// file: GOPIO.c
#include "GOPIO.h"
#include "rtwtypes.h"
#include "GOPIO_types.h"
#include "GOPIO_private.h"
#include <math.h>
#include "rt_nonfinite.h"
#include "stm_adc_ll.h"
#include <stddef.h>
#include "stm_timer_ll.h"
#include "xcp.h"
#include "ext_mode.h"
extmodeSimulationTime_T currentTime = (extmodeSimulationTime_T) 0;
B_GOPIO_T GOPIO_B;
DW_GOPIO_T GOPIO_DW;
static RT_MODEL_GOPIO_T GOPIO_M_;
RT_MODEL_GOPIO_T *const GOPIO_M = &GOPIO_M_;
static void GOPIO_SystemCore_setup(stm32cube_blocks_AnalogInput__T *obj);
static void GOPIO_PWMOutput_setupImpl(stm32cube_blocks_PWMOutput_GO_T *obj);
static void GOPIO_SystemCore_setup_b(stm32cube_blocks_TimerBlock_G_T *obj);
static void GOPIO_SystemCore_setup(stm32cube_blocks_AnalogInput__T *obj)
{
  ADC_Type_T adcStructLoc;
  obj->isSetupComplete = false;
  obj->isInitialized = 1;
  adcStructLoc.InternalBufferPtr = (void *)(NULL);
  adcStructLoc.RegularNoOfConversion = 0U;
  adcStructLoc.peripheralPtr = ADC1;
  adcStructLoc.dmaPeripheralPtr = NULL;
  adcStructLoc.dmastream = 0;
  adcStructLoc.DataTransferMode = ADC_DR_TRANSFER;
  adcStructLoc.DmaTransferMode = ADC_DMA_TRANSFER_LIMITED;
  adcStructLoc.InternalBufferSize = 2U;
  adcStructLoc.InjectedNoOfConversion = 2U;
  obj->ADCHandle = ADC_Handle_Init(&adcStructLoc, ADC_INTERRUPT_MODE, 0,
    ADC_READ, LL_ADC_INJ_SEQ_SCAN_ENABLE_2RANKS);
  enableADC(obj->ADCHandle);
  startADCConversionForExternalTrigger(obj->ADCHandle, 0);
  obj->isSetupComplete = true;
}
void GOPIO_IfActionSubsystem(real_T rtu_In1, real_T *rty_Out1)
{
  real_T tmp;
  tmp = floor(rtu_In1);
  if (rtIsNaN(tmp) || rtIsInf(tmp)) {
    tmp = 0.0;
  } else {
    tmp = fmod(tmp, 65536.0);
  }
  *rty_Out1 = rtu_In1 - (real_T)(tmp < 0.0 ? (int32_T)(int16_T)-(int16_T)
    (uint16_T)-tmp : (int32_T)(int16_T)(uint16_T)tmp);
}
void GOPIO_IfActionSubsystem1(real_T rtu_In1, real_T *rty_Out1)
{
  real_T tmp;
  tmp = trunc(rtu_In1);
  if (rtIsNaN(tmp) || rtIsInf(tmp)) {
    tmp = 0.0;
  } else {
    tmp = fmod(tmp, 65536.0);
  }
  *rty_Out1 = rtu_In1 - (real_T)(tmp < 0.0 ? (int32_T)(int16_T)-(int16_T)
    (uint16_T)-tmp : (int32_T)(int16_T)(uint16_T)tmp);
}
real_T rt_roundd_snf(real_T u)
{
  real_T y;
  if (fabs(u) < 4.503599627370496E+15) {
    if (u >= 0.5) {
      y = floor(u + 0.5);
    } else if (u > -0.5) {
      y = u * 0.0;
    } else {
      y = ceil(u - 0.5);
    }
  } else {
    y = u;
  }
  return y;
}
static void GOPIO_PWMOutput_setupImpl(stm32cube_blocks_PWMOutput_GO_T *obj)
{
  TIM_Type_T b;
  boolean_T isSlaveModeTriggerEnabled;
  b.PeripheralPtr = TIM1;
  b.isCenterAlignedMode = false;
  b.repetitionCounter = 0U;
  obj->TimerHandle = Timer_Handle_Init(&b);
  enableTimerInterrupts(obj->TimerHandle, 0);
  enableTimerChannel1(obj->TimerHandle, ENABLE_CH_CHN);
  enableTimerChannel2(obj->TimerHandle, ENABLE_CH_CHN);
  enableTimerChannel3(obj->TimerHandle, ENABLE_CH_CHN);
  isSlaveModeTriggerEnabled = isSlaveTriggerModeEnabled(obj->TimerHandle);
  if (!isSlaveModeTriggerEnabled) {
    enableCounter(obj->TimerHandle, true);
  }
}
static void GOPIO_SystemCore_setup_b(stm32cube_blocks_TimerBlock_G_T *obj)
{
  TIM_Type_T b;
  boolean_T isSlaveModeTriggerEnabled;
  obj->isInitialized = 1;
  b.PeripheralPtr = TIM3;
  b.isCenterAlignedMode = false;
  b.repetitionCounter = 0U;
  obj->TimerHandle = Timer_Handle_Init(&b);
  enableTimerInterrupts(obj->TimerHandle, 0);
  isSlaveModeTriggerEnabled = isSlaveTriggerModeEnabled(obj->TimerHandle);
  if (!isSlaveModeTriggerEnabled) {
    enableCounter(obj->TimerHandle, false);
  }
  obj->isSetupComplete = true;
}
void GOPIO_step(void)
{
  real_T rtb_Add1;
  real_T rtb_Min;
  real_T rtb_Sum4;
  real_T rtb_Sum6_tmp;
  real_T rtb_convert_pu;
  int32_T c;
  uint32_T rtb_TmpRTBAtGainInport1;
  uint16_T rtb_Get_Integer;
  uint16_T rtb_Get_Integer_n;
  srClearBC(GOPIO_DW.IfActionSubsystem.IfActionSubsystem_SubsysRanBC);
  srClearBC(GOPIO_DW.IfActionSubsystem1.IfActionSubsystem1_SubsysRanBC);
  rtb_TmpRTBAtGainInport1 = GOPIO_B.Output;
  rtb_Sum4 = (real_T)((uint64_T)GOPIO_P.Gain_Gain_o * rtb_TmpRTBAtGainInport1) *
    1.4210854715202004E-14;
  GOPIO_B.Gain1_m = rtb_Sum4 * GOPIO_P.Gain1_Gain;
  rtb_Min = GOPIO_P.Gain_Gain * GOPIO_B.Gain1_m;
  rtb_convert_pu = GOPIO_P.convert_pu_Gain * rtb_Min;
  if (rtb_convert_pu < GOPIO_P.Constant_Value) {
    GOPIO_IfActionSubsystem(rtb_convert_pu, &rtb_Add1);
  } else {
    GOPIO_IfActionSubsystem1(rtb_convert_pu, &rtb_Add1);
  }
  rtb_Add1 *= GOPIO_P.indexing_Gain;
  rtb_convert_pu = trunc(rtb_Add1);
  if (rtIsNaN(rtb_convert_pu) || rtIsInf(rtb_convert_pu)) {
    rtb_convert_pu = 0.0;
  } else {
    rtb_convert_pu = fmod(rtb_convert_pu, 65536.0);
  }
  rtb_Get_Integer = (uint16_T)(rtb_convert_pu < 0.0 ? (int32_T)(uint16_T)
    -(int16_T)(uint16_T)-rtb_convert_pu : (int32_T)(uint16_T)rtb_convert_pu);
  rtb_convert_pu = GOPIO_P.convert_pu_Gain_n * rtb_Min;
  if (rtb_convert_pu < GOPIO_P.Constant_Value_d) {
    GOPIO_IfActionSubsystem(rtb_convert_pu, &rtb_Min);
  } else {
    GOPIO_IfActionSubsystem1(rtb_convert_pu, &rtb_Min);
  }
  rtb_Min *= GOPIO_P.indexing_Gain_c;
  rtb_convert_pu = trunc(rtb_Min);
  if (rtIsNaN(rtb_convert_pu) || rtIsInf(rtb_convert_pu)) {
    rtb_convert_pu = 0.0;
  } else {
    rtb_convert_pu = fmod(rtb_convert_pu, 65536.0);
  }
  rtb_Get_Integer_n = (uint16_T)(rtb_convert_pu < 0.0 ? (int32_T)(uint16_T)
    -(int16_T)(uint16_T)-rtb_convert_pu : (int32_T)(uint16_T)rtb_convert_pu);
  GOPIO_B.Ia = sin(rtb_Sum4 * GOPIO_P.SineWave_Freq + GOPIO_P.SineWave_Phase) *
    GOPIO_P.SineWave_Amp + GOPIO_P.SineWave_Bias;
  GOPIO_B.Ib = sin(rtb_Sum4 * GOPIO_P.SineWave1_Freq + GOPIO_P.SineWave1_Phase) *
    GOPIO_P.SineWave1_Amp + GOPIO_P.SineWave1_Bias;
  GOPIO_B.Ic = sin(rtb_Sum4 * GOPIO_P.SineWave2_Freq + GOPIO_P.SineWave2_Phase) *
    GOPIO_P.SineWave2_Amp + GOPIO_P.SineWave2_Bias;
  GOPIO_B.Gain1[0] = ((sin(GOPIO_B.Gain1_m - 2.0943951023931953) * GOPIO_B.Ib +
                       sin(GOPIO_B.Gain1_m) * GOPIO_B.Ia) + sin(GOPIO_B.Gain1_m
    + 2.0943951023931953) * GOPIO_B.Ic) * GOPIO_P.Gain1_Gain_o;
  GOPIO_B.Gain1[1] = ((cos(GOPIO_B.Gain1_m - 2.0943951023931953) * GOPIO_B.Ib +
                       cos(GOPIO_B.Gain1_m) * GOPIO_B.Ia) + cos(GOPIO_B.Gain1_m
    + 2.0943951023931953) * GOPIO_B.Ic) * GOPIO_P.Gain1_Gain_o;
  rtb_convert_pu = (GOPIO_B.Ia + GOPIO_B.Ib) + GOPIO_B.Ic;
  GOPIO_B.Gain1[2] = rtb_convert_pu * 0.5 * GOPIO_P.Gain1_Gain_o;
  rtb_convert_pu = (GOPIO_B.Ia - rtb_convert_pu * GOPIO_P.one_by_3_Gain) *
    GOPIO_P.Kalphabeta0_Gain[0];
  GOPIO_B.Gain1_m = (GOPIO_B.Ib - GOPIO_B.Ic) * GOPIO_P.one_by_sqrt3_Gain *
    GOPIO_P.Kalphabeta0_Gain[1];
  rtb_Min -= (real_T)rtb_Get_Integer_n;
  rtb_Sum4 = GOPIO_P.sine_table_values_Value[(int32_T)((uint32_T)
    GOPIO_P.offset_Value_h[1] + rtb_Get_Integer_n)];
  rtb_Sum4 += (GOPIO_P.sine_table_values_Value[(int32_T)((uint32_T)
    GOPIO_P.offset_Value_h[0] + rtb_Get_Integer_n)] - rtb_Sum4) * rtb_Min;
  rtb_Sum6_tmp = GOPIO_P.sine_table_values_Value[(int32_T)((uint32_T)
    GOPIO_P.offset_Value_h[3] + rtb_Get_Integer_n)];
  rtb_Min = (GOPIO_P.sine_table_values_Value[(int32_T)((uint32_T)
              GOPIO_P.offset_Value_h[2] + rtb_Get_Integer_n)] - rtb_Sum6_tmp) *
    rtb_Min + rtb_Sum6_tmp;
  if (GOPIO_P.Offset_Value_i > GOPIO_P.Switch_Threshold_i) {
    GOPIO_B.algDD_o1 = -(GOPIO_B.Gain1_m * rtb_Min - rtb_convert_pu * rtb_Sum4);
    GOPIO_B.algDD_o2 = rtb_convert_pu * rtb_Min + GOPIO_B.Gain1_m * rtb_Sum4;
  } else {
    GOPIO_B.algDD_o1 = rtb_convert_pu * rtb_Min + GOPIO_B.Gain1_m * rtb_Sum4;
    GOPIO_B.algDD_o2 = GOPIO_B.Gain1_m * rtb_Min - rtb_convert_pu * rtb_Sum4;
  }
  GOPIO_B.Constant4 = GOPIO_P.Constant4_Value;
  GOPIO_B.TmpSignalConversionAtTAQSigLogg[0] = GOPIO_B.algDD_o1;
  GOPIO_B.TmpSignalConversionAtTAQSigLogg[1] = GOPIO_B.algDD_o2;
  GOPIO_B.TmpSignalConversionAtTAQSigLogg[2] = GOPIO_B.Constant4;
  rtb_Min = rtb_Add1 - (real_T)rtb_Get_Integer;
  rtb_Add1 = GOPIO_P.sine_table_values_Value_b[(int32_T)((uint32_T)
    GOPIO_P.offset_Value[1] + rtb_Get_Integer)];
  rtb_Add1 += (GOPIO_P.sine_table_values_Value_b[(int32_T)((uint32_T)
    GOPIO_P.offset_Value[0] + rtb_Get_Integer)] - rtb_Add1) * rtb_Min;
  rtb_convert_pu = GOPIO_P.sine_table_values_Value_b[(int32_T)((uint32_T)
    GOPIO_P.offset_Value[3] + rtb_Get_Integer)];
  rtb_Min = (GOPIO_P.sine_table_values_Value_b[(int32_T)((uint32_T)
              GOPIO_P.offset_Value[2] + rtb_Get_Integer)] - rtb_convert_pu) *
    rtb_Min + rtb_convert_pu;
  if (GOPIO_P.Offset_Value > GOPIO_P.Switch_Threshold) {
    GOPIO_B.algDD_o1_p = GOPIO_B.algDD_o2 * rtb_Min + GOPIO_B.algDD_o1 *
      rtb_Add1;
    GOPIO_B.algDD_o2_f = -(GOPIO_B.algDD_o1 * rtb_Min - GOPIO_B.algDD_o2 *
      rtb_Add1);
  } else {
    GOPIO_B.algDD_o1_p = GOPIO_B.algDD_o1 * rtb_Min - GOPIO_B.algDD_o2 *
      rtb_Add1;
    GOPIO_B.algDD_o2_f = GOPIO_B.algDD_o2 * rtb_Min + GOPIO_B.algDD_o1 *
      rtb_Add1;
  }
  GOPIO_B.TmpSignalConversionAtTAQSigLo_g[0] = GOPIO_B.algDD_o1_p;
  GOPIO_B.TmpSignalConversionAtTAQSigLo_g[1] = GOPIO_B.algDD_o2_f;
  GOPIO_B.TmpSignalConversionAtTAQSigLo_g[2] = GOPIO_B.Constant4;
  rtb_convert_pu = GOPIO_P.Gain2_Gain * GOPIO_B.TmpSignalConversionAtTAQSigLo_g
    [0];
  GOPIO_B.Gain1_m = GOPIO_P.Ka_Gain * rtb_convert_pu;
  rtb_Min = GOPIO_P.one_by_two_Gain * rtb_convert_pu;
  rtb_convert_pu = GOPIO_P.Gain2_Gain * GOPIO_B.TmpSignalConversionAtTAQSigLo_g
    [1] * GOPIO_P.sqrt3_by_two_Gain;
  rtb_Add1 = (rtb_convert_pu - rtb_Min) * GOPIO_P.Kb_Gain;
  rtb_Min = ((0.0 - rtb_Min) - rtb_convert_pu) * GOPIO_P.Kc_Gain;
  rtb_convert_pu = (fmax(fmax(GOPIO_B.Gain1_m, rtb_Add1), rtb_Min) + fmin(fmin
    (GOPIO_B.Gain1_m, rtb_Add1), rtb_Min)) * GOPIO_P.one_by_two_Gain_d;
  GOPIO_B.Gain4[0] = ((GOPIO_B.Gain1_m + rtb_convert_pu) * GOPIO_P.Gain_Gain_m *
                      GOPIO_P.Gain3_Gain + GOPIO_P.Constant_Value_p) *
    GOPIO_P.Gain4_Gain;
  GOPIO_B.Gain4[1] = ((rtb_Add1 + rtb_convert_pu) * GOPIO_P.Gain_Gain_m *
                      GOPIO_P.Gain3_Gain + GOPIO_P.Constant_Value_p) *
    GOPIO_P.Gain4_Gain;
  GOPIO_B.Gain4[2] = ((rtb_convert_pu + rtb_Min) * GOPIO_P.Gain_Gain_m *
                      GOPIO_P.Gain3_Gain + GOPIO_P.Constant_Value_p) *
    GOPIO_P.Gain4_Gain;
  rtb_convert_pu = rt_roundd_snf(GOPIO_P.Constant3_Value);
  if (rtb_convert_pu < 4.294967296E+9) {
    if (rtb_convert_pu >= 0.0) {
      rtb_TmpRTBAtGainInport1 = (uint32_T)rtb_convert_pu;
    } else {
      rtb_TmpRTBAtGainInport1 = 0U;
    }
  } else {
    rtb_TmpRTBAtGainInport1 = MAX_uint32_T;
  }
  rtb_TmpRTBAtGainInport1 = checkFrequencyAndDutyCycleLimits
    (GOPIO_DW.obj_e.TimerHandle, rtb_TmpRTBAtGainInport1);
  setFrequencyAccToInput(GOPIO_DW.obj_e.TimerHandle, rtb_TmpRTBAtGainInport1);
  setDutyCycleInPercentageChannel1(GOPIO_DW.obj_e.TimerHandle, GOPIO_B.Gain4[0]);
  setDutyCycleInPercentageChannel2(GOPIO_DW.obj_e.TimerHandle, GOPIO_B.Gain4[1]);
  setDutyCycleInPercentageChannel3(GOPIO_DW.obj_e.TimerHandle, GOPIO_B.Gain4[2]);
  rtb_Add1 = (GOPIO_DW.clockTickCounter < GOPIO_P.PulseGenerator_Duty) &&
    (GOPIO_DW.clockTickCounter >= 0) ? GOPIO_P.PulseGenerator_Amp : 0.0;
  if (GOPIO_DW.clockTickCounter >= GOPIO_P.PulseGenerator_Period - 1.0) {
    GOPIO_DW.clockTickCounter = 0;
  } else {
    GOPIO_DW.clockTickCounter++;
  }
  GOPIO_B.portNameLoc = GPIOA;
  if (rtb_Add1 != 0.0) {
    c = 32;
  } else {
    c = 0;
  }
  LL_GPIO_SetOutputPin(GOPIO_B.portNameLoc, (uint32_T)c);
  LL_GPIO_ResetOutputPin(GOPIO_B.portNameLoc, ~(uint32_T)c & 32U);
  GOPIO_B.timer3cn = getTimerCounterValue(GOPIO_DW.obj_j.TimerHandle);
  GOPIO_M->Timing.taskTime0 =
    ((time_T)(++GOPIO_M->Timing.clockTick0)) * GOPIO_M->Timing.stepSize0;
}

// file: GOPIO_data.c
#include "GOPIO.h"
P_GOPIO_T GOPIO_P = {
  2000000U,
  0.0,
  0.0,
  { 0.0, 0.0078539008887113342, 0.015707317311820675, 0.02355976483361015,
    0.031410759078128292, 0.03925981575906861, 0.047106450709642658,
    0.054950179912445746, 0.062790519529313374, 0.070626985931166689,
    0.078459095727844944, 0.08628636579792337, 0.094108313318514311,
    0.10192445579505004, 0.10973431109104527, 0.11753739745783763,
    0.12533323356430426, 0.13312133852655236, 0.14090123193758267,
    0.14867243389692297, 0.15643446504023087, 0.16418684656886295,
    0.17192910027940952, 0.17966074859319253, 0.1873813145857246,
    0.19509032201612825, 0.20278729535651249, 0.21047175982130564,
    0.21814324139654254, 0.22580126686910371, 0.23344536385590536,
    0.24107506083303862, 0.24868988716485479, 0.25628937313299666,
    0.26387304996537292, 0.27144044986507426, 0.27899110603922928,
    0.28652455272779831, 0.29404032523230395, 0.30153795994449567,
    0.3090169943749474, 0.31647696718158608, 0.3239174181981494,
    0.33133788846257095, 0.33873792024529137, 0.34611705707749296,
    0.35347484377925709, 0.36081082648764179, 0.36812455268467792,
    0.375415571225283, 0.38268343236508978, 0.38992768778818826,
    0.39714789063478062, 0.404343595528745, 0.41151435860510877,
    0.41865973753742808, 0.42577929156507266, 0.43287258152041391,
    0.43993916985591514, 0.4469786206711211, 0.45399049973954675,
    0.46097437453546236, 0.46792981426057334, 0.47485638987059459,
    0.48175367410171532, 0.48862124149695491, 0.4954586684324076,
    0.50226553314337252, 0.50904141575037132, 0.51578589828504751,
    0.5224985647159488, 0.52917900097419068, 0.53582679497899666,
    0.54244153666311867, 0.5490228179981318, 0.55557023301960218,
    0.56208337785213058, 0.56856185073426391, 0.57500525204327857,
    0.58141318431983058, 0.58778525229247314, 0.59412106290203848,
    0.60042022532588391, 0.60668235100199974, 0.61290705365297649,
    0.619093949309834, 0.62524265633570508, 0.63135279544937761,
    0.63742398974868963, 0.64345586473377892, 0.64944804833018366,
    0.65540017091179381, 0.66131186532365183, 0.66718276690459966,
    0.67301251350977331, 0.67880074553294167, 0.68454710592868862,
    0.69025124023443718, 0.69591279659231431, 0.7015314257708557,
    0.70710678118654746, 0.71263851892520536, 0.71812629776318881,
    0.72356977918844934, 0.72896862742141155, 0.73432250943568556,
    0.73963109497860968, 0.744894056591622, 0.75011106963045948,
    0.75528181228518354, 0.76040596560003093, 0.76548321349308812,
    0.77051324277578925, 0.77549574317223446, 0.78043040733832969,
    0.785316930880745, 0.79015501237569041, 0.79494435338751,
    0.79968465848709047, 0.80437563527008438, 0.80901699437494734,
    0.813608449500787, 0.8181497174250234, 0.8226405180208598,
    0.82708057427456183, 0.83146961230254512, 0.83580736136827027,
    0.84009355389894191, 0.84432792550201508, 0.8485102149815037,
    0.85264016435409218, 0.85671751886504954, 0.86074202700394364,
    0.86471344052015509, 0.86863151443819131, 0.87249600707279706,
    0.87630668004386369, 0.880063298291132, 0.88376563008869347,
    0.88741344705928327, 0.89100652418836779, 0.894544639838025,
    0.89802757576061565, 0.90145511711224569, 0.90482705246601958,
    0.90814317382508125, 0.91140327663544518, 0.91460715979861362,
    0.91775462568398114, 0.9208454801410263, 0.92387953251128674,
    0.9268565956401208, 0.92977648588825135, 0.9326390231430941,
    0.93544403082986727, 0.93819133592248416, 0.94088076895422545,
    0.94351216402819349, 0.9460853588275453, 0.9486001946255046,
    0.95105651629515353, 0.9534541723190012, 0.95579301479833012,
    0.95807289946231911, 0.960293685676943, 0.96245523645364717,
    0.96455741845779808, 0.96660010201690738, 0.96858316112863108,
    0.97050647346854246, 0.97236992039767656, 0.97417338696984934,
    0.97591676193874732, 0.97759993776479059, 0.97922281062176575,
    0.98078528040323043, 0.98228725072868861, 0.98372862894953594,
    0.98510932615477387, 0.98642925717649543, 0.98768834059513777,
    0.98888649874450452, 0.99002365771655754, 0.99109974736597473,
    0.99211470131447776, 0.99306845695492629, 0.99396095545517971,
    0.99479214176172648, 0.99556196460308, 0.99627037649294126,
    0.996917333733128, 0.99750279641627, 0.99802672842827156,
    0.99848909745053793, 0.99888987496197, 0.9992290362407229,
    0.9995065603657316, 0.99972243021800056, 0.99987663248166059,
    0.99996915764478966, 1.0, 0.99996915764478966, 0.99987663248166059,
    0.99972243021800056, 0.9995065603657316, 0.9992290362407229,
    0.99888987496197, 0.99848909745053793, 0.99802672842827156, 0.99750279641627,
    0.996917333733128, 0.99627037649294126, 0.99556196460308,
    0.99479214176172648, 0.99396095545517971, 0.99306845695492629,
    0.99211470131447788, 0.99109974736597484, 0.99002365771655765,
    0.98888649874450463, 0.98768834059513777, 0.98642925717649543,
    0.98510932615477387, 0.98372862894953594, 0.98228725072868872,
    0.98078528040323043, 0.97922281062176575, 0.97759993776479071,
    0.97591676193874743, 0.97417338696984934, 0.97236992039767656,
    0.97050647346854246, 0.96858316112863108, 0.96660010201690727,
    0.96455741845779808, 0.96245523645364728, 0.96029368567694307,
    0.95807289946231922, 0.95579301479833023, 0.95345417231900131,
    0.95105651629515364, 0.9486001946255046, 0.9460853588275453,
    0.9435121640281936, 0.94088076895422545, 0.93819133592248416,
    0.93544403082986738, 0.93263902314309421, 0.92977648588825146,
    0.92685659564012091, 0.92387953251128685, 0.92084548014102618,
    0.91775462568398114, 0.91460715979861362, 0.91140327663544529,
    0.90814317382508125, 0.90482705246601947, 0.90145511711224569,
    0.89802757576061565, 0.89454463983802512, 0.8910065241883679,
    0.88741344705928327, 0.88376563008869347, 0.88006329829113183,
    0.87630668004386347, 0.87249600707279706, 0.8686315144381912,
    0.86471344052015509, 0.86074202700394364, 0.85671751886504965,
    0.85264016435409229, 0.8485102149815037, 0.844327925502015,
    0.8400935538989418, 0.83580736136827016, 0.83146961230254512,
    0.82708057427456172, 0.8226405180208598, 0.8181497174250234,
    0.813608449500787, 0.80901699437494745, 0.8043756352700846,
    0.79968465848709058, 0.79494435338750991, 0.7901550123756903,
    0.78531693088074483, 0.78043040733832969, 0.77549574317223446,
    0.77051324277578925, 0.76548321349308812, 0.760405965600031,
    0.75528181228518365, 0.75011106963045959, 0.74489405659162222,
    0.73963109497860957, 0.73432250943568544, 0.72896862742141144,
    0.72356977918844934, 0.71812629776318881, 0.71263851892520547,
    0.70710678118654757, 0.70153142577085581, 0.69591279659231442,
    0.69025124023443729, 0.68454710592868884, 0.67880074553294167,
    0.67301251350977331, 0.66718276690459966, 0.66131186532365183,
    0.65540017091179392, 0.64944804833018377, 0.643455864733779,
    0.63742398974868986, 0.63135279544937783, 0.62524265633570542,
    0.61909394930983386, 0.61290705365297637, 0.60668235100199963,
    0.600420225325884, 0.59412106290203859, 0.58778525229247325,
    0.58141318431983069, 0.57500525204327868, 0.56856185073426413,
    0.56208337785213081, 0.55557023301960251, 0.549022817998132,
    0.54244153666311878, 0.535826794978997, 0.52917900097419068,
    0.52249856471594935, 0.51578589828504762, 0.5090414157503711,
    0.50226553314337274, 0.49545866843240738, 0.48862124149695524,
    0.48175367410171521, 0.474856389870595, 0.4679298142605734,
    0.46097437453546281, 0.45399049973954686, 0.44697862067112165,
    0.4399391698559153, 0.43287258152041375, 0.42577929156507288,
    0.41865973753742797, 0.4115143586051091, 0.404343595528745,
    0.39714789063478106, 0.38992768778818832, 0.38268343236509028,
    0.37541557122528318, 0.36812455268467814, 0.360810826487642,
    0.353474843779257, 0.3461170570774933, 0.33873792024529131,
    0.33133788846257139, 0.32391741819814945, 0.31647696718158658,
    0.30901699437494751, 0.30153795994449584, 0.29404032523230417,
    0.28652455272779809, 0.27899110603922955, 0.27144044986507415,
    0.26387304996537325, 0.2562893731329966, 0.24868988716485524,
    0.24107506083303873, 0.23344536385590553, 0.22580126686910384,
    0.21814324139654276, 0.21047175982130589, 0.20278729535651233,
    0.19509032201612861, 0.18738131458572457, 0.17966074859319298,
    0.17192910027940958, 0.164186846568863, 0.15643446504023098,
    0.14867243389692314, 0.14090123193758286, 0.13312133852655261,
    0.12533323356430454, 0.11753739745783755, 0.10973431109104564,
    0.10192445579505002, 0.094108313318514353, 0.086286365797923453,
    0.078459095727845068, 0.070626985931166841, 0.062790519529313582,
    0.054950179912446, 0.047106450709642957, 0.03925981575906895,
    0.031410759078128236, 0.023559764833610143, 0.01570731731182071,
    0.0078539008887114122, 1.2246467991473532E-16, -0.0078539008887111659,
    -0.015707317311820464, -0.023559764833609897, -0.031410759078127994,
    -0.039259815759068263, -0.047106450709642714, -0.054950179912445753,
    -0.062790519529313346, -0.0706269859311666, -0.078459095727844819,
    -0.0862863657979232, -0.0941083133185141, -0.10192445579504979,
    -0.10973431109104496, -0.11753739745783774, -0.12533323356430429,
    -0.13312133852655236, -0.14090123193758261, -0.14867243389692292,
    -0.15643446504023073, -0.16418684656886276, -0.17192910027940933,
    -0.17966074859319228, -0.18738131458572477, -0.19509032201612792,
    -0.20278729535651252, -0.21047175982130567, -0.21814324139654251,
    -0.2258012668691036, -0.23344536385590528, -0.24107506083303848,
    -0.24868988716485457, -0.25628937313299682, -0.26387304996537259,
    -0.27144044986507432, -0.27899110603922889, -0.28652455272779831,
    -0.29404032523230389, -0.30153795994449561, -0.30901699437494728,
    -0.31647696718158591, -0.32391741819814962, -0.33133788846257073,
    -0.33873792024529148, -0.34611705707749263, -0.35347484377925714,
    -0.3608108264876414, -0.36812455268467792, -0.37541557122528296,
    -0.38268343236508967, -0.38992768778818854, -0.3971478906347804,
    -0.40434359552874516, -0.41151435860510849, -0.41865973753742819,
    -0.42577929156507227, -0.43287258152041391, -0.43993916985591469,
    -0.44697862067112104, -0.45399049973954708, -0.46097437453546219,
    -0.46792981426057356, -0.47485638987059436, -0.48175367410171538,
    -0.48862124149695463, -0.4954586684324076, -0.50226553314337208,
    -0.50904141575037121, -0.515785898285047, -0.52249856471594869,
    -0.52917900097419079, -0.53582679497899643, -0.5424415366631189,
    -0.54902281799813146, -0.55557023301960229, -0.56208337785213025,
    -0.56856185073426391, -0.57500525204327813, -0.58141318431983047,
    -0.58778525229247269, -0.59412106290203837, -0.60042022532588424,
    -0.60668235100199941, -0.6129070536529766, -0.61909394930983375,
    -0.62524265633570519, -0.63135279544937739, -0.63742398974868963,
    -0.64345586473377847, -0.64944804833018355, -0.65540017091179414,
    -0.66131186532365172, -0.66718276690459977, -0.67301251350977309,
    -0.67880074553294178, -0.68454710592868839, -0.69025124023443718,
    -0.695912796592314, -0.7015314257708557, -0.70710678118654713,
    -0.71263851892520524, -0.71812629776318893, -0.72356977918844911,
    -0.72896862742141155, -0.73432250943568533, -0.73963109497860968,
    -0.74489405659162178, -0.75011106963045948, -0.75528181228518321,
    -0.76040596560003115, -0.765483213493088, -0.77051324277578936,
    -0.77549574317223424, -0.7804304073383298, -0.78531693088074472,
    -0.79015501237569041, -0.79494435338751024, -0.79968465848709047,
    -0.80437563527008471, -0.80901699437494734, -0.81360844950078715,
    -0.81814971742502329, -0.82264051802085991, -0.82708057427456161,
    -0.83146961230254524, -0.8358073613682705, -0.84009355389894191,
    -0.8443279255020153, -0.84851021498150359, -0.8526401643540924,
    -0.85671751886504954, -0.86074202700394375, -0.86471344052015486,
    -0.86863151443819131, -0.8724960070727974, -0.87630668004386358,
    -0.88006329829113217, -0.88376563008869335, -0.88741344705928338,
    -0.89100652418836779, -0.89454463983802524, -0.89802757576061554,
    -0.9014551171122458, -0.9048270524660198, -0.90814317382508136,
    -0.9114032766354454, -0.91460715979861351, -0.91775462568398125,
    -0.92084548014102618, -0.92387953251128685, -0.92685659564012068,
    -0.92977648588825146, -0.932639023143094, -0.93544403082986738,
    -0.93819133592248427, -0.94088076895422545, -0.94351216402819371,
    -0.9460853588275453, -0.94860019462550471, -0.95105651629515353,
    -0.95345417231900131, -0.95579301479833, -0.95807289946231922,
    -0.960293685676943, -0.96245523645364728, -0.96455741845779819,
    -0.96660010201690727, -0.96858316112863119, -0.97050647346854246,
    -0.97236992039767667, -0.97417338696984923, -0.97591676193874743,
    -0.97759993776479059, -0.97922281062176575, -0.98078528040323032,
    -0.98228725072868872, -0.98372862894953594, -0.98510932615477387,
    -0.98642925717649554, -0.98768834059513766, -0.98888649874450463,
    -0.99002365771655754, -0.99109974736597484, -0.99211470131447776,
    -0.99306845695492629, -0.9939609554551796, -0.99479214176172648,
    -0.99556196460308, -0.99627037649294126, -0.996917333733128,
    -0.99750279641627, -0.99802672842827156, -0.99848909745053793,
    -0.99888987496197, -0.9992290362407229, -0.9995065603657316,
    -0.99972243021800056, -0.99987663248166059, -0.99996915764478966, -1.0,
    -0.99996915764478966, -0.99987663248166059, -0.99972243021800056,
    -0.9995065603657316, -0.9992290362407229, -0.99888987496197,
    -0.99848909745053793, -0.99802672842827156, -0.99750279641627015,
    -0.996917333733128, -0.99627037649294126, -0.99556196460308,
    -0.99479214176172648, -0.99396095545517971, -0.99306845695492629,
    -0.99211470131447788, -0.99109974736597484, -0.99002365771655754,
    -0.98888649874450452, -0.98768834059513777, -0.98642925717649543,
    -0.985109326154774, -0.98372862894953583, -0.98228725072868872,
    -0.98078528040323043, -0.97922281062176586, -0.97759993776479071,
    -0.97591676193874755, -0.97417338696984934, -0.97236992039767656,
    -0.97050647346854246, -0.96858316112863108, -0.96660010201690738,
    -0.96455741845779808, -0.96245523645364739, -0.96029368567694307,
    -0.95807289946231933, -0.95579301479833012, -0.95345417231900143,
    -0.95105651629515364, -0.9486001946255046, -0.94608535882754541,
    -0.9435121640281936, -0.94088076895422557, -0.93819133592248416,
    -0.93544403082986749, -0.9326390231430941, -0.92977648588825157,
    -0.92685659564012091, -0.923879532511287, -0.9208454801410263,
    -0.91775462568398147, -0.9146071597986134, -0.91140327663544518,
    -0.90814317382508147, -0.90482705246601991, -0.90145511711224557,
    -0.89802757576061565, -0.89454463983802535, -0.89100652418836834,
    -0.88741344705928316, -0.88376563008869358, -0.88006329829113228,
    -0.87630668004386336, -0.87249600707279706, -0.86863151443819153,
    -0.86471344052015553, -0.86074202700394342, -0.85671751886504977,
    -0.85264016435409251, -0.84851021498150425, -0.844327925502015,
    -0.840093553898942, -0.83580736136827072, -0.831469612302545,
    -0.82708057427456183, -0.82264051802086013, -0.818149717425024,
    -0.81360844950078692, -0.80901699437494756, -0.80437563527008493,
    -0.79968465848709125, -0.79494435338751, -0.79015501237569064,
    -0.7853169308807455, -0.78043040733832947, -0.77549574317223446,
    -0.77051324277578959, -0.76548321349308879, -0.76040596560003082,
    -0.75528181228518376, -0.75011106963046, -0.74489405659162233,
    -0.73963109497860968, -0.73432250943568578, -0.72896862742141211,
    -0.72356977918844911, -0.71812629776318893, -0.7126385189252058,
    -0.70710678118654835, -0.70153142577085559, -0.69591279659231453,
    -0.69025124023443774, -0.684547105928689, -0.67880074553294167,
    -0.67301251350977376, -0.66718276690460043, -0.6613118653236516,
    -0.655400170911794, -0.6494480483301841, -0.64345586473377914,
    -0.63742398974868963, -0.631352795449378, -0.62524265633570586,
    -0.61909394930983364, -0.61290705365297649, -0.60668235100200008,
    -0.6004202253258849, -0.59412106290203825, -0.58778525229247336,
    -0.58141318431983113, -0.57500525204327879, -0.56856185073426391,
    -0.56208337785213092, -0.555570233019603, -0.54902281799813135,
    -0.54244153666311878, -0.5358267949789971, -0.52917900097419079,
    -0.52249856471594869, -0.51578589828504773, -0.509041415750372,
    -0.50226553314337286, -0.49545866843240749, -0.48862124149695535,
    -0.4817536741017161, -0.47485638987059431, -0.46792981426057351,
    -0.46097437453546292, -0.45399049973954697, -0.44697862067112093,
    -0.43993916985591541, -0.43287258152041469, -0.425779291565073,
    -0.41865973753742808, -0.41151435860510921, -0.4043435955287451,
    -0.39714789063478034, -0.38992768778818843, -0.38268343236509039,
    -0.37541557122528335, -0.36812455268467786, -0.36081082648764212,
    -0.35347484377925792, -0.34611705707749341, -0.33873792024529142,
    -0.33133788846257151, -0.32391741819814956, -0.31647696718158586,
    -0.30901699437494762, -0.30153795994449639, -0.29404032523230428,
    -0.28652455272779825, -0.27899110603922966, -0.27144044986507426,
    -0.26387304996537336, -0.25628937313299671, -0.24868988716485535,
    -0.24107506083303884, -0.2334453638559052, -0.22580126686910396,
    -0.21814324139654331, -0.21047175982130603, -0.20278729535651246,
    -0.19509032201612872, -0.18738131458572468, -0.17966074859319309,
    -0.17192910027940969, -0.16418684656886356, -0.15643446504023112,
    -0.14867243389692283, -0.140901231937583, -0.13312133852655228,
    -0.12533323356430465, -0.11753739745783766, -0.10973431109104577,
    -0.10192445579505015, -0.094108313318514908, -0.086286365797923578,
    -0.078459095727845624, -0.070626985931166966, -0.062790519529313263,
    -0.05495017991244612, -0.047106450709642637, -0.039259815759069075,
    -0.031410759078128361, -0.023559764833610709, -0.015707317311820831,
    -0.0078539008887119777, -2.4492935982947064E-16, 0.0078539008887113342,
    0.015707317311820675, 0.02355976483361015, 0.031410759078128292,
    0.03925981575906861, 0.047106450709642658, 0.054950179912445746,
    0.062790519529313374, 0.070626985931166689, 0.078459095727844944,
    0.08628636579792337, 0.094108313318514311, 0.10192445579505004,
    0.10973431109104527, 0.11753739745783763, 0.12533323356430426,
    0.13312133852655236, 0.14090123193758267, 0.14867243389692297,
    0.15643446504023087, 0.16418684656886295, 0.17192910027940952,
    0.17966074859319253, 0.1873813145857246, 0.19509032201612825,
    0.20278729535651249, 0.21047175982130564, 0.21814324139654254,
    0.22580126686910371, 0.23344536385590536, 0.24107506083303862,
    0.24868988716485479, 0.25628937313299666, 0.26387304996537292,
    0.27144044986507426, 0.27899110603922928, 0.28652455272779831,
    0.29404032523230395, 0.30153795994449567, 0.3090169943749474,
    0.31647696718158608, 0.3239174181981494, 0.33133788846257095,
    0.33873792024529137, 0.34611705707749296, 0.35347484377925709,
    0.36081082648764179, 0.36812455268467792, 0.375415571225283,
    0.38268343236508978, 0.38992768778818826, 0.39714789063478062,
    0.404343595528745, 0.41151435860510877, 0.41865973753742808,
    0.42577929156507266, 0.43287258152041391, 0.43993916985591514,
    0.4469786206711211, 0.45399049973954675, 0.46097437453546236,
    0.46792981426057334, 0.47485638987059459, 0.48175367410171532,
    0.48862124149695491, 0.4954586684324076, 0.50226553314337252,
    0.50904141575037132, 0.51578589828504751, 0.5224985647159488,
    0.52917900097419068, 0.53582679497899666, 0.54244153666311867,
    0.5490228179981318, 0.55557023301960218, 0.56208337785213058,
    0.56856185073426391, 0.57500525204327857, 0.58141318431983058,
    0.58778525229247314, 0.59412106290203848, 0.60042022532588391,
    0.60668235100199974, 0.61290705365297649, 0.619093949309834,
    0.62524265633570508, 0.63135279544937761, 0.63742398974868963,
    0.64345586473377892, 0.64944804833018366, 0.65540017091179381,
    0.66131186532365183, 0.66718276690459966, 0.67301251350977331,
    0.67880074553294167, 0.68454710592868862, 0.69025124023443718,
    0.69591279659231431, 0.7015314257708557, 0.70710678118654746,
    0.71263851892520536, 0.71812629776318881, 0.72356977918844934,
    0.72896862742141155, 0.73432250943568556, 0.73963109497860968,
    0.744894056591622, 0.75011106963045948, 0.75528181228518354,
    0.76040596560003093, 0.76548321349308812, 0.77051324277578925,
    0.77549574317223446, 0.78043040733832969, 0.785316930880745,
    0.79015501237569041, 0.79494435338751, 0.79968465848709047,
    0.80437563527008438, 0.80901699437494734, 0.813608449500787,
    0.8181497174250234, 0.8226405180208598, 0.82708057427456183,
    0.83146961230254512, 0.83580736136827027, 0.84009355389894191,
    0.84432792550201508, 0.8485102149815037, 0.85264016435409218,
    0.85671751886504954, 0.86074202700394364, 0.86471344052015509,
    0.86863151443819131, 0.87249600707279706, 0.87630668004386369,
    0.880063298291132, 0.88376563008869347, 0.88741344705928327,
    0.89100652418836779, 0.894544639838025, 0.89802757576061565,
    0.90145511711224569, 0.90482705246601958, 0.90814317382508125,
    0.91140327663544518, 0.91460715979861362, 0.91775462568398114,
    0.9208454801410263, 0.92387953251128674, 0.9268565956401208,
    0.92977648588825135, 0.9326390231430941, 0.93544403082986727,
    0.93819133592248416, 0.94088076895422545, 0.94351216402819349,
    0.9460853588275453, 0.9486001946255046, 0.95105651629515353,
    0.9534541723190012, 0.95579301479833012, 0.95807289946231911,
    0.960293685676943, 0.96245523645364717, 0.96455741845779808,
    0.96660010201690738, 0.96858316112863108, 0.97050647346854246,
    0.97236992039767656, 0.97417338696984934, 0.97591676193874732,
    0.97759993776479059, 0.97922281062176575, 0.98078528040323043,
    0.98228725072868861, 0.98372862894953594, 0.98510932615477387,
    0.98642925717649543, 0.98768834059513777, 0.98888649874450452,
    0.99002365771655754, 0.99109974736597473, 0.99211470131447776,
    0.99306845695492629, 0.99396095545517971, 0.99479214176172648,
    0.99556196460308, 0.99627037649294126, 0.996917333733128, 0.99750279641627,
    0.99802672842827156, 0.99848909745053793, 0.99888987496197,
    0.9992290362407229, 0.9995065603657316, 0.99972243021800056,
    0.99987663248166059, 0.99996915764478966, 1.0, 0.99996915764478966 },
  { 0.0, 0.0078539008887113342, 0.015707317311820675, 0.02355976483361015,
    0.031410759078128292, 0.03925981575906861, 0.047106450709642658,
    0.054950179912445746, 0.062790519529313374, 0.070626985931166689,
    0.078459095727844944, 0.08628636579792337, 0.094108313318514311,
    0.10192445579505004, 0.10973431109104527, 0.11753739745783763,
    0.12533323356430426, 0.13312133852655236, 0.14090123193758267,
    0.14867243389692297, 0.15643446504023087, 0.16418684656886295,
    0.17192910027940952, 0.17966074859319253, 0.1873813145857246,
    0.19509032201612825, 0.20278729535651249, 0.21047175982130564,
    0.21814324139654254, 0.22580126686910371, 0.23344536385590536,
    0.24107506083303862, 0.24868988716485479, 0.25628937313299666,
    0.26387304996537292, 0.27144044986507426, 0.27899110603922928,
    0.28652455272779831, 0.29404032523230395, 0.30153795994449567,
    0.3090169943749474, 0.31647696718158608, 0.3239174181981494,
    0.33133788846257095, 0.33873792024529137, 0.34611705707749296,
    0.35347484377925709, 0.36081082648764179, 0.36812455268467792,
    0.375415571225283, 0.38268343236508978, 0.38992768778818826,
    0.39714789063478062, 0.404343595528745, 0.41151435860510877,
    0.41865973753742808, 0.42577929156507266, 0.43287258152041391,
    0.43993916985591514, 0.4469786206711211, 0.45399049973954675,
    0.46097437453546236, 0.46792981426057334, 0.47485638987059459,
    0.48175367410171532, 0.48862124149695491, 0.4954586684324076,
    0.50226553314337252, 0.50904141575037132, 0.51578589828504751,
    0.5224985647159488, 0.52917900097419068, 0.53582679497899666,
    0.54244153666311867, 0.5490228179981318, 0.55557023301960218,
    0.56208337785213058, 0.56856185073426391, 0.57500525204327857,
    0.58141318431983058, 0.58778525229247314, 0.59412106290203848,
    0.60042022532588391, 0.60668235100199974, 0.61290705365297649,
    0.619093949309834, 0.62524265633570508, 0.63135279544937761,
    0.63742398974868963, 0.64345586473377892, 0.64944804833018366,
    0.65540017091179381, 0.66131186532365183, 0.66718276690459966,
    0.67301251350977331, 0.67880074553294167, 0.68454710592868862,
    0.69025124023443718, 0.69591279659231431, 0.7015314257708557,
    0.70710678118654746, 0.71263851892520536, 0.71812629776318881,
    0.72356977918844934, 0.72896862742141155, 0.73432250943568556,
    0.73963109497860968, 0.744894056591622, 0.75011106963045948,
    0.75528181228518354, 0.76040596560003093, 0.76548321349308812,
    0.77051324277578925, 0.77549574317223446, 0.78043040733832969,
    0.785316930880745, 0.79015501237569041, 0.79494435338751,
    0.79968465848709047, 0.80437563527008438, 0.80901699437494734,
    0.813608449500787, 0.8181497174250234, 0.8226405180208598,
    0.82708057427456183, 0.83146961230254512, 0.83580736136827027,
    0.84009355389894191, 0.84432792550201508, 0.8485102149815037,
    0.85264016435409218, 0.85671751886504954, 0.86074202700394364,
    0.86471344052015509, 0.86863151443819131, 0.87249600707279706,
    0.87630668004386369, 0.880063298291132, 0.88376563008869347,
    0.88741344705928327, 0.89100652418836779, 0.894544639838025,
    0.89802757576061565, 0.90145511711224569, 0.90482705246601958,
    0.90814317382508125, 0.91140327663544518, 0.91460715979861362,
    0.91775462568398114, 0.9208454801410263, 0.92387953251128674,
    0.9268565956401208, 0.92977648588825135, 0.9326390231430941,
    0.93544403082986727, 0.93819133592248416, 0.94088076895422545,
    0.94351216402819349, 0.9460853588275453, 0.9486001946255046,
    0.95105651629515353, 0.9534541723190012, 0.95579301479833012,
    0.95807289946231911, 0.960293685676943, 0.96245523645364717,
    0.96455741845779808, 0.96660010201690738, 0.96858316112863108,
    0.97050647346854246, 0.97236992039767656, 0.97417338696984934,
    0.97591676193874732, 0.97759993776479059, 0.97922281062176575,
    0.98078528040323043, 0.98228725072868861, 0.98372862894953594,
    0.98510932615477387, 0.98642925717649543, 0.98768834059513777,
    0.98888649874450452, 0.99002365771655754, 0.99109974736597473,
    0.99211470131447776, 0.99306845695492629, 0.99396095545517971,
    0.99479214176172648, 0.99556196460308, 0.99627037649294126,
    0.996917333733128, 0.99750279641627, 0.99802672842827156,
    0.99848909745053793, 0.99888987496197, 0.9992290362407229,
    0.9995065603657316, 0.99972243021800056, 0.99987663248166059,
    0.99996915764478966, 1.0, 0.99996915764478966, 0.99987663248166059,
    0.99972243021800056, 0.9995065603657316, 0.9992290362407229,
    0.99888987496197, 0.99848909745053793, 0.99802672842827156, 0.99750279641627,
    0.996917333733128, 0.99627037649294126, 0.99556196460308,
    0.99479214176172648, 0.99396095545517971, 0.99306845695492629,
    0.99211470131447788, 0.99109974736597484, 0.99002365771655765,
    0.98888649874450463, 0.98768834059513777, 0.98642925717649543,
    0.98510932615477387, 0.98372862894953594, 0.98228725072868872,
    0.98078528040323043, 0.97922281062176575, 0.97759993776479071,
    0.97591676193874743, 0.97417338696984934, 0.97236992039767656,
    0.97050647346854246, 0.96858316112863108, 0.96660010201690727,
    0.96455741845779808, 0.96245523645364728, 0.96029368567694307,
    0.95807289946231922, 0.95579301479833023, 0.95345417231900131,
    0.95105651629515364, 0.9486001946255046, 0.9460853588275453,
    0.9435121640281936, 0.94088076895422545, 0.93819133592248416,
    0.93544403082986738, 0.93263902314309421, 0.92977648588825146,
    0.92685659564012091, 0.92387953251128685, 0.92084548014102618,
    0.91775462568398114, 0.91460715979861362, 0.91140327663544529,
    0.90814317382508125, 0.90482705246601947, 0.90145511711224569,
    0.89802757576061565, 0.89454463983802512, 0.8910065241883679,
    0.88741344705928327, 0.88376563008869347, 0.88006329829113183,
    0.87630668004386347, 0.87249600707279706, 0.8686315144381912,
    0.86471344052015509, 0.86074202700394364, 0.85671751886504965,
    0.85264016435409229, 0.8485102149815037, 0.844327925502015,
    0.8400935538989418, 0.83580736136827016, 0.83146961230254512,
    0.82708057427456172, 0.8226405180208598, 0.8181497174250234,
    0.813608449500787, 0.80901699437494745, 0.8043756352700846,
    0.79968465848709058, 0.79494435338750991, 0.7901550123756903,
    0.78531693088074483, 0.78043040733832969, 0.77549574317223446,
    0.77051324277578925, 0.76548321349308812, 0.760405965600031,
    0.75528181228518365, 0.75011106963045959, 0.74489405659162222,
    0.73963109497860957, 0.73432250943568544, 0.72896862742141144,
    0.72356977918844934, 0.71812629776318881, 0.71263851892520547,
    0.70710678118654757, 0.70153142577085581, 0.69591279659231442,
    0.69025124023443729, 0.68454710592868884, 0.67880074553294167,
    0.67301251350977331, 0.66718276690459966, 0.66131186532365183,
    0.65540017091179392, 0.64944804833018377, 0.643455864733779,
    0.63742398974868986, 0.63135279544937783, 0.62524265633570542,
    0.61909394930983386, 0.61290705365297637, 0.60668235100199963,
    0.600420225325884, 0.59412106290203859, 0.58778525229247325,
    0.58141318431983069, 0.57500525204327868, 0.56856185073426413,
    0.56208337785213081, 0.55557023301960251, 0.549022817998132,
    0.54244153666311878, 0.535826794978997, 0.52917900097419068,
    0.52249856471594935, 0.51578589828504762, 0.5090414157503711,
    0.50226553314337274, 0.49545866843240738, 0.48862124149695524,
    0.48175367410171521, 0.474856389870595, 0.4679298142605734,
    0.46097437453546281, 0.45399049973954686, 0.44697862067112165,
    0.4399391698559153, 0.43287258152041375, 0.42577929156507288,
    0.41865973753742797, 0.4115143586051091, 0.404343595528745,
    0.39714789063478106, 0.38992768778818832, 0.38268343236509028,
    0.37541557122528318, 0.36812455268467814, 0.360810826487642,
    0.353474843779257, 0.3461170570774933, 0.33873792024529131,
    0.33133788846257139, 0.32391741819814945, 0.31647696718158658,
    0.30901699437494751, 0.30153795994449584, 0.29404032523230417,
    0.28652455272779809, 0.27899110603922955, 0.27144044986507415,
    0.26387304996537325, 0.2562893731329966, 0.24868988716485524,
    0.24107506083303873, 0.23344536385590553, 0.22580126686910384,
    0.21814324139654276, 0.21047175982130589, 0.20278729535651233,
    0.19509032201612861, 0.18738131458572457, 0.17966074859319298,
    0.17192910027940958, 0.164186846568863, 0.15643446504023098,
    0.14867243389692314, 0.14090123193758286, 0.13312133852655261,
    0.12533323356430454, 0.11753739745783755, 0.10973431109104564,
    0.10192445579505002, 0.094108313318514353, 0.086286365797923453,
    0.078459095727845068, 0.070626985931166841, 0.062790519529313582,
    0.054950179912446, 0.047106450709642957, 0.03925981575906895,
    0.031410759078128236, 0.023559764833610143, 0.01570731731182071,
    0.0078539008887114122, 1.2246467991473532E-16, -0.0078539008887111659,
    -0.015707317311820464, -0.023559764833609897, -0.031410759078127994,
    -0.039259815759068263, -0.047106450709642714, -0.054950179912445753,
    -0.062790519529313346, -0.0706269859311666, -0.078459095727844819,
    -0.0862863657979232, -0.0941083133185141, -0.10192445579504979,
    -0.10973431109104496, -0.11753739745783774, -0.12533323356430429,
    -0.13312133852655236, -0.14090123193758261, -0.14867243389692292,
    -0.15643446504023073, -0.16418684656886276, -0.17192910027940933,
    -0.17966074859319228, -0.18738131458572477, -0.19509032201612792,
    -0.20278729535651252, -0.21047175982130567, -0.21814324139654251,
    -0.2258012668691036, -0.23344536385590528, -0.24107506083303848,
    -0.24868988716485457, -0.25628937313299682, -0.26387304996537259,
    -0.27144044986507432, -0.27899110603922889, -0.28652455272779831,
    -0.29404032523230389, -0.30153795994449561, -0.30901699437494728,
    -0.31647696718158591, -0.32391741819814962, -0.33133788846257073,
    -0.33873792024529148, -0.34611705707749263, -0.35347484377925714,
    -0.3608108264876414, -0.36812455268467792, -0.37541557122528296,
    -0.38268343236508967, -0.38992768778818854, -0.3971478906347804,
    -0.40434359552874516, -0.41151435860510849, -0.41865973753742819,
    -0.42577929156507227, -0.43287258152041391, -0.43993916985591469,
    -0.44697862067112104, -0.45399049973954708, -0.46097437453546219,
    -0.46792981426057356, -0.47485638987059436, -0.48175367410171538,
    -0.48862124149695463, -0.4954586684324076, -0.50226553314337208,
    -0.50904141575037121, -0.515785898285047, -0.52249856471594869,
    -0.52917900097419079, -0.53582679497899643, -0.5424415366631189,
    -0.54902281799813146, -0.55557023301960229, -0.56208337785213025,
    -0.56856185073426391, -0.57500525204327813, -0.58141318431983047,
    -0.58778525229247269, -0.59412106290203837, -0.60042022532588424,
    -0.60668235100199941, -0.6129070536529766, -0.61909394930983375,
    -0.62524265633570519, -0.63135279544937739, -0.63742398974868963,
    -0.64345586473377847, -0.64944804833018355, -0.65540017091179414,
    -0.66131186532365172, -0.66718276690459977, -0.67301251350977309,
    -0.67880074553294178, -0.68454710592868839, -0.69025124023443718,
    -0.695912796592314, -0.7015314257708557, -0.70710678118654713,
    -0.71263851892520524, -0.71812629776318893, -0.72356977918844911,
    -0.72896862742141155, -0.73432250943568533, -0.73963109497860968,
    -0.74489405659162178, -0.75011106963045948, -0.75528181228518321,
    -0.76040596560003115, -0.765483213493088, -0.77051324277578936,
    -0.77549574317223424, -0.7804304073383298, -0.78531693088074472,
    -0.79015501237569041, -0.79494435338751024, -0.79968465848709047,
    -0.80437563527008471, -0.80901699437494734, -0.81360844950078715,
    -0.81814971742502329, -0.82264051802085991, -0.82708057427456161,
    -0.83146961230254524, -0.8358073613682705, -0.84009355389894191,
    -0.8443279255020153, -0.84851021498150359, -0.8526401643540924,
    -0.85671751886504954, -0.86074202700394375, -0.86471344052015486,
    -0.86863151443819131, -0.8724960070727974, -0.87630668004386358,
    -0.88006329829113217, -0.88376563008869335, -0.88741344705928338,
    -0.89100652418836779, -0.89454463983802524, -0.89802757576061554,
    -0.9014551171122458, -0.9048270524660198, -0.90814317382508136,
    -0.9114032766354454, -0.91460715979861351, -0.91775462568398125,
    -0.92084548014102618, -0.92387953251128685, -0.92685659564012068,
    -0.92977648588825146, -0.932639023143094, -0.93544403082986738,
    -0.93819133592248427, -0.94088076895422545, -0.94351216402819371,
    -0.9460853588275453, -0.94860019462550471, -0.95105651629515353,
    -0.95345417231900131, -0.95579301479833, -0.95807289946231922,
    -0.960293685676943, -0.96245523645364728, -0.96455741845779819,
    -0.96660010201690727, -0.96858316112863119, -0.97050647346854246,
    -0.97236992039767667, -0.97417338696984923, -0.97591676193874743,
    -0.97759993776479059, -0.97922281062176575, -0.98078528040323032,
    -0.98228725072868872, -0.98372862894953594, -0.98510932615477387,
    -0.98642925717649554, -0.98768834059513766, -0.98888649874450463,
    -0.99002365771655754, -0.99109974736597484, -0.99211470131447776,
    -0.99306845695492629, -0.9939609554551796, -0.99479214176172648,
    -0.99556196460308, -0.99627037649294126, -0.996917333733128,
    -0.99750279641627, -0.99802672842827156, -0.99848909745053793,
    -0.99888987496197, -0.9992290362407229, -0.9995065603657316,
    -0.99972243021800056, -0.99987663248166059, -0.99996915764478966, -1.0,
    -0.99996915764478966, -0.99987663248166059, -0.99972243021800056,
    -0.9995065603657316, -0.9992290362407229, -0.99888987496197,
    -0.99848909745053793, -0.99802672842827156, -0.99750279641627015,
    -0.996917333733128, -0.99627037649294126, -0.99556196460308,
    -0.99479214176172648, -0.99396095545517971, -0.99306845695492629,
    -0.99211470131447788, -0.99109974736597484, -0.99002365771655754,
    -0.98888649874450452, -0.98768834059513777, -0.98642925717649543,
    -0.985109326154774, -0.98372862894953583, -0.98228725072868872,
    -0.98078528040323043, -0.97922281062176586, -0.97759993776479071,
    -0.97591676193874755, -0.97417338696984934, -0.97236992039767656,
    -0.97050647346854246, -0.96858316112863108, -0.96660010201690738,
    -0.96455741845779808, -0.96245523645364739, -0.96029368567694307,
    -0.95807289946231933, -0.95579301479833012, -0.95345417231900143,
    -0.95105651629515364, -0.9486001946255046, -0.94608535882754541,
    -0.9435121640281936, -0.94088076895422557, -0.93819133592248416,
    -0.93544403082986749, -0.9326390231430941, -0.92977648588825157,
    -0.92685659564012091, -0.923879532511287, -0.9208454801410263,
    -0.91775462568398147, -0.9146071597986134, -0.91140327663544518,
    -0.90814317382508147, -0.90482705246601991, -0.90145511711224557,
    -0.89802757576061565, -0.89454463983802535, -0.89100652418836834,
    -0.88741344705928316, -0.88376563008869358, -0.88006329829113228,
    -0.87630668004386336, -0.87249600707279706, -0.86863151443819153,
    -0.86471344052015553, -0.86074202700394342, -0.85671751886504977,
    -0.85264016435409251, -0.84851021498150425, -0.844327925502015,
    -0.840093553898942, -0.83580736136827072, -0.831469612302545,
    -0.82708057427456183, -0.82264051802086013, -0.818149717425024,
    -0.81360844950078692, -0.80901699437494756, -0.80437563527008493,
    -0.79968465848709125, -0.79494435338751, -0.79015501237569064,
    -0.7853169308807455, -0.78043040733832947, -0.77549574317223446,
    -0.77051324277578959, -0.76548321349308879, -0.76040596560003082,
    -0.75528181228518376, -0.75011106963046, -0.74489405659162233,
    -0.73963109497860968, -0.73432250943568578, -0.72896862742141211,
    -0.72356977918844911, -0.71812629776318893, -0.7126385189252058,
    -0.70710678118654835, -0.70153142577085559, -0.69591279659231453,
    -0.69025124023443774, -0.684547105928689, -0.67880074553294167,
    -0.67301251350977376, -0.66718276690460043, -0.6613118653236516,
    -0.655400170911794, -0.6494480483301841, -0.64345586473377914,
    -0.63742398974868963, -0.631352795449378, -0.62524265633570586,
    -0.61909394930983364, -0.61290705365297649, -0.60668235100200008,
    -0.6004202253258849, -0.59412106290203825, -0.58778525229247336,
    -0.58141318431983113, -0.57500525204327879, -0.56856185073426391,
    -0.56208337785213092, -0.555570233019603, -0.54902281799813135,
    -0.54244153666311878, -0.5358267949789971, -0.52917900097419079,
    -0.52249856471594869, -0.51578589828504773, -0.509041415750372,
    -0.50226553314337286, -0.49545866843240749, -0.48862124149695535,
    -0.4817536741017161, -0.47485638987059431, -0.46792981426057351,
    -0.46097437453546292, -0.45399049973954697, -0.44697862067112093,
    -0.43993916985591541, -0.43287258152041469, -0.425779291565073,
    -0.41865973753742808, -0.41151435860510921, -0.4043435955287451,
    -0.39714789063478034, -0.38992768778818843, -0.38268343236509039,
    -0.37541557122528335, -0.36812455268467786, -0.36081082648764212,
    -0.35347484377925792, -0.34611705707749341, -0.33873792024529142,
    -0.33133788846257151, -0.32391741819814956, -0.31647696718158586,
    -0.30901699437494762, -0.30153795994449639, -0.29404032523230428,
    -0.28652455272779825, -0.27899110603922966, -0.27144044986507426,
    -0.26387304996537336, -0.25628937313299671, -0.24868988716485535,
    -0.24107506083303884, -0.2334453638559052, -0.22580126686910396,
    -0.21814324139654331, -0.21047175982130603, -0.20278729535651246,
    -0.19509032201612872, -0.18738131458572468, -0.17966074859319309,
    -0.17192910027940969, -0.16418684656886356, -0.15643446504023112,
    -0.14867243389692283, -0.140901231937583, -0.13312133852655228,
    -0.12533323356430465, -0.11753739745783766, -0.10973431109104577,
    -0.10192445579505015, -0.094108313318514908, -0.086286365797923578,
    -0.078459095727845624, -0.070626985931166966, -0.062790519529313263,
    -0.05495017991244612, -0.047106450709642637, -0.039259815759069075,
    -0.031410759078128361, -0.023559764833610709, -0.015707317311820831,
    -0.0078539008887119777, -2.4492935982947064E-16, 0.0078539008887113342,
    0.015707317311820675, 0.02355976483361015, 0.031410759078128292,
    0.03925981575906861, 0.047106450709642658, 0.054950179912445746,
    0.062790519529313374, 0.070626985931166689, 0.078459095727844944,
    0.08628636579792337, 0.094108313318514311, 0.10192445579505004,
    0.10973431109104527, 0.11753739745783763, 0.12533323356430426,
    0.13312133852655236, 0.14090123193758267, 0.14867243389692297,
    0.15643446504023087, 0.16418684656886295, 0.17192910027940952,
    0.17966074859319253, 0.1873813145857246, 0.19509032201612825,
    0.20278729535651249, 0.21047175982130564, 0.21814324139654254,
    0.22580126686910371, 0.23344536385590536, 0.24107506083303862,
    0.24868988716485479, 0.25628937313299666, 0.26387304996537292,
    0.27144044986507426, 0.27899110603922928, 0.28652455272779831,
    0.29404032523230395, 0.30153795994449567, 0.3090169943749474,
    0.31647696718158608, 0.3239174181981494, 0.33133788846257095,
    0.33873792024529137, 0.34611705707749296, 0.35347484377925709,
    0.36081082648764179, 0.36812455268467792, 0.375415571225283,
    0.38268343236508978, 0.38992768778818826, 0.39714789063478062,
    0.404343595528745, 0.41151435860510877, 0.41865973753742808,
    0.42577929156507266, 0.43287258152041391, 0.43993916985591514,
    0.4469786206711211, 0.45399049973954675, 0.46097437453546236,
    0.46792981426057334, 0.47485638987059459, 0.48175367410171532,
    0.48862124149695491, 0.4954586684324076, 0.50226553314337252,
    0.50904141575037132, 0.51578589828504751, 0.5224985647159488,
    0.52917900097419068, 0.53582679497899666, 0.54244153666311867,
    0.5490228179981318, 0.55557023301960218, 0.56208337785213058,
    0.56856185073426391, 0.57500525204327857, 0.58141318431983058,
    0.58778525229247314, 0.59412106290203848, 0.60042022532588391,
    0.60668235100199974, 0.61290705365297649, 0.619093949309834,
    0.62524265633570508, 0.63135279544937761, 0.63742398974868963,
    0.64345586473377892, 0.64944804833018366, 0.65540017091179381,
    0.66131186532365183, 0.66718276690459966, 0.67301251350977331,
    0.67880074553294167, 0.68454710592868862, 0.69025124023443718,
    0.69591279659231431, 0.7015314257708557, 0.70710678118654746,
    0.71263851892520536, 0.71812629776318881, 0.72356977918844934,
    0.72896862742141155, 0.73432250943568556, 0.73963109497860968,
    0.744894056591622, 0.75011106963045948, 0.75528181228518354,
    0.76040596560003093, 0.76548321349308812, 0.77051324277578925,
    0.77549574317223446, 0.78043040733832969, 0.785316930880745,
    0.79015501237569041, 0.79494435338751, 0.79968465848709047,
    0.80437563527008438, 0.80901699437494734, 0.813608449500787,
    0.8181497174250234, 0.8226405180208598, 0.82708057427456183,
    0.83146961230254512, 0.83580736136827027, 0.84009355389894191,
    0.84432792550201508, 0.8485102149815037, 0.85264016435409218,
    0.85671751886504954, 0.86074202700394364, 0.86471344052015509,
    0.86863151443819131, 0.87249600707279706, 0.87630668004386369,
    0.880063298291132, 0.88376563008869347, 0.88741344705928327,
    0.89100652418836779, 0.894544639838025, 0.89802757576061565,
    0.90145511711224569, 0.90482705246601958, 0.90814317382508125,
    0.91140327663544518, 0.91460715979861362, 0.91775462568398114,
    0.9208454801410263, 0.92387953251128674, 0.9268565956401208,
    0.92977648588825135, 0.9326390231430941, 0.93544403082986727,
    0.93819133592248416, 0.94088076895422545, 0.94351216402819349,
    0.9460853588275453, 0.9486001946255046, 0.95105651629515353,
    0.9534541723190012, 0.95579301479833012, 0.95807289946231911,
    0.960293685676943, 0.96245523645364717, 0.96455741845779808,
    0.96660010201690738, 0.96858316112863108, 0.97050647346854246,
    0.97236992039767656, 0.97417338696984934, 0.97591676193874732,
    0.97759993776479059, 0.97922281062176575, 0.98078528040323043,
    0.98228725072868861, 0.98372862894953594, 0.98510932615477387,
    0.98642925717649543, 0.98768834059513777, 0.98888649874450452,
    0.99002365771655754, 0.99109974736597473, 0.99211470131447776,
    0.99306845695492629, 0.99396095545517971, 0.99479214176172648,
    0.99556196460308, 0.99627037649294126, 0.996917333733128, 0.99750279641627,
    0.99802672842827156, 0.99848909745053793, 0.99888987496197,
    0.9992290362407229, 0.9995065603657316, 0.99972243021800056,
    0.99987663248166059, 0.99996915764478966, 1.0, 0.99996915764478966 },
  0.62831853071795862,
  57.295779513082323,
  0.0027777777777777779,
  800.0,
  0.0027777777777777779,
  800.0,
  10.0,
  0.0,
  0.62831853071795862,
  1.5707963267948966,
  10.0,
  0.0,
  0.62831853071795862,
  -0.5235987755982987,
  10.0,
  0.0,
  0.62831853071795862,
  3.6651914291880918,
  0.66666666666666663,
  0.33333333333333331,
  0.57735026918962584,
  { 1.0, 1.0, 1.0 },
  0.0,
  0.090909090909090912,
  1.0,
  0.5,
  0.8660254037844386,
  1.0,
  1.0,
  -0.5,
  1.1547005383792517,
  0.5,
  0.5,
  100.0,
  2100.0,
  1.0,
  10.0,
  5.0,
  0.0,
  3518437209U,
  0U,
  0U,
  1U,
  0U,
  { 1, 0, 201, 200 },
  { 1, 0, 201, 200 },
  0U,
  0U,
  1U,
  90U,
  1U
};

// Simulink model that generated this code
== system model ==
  PWMOutput : stm32f4xxblockslib/PWM Output  <- 1: Constant3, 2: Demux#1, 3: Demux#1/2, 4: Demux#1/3
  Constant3 : Constant  Value=2100
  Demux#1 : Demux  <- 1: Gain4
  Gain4 : Gain  Gain=100  <- 1: Sum#1
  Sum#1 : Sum  <- 1: Gain3, 2: Constant
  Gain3 : Gain  Gain=1/2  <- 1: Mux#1
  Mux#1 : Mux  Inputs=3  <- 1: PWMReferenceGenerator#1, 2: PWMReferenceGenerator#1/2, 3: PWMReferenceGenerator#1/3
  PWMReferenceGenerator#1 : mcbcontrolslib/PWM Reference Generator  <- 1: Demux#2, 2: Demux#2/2
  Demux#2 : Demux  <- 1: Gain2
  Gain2 : Gain  Gain=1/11  <- 1: InverseParkTransform#1
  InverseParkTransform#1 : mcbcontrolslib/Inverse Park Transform  <- 1: Mux#2, 2: RadianstoDegrees#1
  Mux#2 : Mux  Inputs=3  <- 1: ParkTransform#1, 2: ParkTransform#1/2, 3: Constant4
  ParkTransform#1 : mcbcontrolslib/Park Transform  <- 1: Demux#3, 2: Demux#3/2, 3: RadianstoDegrees#1
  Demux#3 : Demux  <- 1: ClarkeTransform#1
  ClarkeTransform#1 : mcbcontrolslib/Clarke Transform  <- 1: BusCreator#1
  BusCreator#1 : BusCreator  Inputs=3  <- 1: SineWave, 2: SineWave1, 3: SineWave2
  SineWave : Sin  Amplitude=10  Frequency=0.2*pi  Phase=pi/2  <- 1: DataTypeConversion#1
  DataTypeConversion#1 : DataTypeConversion  <- 1: Gain
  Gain : Gain  Gain=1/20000  <- 1: Subsystem#1
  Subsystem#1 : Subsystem  <- Trigger: VariantSource#1
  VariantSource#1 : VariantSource  <- 1: HardwareInterrupt#1, 2: FunctionCallGenerator#1
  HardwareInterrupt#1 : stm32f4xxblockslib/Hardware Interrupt
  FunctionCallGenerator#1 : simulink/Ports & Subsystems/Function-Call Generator
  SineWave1 : Sin  Amplitude=10  Frequency=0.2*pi  Phase=-2/3*pi+pi/2  <- 1: DataTypeConversion#1
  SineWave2 : Sin  Amplitude=10  Frequency=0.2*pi  Phase=2/3*pi+pi/2  <- 1: DataTypeConversion#1
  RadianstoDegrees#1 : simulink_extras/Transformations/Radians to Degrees  <- 1: Gain1
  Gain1 : Gain  Gain=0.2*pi  <- 1: DataTypeConversion#1
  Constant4 : Constant  Value=0
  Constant : Constant  Value=0.5
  Timer : stm32blockslib/Timer
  ParkTransform#2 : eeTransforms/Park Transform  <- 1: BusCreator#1, 2: Gain1
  DigitalPortWrite#1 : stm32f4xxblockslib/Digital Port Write  <- 1: PulseGenerator
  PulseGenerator : DiscretePulseGenerator  Period=10  PulseWidth=5
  PIDController#1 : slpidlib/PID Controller  Controller=PI  Form=Parallel  TimeDomain=Discrete-time  IntegratorMethod=Forward Euler  P=1  I=1  D=0  N=100  InitialConditionForIntegrator=0  ExternalReset=none  LimitOutput=on  UpperSaturationLimit=1  LowerSaturationLimit=-1
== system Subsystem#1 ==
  TriggerPort#1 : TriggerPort  TriggerType=function-call
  Outport#1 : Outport  <- 1: CounterLimited#1
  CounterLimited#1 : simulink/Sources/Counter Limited  uplimit=2000000
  Outport#2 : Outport  <- 1: AnalogtoDigitalConverter#1
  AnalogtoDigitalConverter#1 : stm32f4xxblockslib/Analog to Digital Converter
